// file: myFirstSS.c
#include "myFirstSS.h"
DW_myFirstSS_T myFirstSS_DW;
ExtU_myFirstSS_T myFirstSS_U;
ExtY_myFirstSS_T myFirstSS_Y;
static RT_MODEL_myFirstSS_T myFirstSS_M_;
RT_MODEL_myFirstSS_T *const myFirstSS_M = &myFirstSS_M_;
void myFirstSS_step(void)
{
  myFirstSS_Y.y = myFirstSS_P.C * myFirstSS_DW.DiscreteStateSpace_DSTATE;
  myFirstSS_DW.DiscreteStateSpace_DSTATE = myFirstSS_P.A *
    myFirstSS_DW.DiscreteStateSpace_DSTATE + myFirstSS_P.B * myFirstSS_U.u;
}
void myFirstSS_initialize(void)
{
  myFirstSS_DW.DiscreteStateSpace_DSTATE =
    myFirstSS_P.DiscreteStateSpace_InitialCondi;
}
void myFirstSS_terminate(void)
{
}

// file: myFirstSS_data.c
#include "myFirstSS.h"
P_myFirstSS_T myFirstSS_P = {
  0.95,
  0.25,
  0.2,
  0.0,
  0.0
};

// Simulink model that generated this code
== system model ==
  Inport#1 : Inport
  Outport#1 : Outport  <- 1: DiscreteStateSpace
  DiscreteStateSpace : DiscreteStateSpace  A=A  B=B  C=C  D=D  <- 1: Inport#1
